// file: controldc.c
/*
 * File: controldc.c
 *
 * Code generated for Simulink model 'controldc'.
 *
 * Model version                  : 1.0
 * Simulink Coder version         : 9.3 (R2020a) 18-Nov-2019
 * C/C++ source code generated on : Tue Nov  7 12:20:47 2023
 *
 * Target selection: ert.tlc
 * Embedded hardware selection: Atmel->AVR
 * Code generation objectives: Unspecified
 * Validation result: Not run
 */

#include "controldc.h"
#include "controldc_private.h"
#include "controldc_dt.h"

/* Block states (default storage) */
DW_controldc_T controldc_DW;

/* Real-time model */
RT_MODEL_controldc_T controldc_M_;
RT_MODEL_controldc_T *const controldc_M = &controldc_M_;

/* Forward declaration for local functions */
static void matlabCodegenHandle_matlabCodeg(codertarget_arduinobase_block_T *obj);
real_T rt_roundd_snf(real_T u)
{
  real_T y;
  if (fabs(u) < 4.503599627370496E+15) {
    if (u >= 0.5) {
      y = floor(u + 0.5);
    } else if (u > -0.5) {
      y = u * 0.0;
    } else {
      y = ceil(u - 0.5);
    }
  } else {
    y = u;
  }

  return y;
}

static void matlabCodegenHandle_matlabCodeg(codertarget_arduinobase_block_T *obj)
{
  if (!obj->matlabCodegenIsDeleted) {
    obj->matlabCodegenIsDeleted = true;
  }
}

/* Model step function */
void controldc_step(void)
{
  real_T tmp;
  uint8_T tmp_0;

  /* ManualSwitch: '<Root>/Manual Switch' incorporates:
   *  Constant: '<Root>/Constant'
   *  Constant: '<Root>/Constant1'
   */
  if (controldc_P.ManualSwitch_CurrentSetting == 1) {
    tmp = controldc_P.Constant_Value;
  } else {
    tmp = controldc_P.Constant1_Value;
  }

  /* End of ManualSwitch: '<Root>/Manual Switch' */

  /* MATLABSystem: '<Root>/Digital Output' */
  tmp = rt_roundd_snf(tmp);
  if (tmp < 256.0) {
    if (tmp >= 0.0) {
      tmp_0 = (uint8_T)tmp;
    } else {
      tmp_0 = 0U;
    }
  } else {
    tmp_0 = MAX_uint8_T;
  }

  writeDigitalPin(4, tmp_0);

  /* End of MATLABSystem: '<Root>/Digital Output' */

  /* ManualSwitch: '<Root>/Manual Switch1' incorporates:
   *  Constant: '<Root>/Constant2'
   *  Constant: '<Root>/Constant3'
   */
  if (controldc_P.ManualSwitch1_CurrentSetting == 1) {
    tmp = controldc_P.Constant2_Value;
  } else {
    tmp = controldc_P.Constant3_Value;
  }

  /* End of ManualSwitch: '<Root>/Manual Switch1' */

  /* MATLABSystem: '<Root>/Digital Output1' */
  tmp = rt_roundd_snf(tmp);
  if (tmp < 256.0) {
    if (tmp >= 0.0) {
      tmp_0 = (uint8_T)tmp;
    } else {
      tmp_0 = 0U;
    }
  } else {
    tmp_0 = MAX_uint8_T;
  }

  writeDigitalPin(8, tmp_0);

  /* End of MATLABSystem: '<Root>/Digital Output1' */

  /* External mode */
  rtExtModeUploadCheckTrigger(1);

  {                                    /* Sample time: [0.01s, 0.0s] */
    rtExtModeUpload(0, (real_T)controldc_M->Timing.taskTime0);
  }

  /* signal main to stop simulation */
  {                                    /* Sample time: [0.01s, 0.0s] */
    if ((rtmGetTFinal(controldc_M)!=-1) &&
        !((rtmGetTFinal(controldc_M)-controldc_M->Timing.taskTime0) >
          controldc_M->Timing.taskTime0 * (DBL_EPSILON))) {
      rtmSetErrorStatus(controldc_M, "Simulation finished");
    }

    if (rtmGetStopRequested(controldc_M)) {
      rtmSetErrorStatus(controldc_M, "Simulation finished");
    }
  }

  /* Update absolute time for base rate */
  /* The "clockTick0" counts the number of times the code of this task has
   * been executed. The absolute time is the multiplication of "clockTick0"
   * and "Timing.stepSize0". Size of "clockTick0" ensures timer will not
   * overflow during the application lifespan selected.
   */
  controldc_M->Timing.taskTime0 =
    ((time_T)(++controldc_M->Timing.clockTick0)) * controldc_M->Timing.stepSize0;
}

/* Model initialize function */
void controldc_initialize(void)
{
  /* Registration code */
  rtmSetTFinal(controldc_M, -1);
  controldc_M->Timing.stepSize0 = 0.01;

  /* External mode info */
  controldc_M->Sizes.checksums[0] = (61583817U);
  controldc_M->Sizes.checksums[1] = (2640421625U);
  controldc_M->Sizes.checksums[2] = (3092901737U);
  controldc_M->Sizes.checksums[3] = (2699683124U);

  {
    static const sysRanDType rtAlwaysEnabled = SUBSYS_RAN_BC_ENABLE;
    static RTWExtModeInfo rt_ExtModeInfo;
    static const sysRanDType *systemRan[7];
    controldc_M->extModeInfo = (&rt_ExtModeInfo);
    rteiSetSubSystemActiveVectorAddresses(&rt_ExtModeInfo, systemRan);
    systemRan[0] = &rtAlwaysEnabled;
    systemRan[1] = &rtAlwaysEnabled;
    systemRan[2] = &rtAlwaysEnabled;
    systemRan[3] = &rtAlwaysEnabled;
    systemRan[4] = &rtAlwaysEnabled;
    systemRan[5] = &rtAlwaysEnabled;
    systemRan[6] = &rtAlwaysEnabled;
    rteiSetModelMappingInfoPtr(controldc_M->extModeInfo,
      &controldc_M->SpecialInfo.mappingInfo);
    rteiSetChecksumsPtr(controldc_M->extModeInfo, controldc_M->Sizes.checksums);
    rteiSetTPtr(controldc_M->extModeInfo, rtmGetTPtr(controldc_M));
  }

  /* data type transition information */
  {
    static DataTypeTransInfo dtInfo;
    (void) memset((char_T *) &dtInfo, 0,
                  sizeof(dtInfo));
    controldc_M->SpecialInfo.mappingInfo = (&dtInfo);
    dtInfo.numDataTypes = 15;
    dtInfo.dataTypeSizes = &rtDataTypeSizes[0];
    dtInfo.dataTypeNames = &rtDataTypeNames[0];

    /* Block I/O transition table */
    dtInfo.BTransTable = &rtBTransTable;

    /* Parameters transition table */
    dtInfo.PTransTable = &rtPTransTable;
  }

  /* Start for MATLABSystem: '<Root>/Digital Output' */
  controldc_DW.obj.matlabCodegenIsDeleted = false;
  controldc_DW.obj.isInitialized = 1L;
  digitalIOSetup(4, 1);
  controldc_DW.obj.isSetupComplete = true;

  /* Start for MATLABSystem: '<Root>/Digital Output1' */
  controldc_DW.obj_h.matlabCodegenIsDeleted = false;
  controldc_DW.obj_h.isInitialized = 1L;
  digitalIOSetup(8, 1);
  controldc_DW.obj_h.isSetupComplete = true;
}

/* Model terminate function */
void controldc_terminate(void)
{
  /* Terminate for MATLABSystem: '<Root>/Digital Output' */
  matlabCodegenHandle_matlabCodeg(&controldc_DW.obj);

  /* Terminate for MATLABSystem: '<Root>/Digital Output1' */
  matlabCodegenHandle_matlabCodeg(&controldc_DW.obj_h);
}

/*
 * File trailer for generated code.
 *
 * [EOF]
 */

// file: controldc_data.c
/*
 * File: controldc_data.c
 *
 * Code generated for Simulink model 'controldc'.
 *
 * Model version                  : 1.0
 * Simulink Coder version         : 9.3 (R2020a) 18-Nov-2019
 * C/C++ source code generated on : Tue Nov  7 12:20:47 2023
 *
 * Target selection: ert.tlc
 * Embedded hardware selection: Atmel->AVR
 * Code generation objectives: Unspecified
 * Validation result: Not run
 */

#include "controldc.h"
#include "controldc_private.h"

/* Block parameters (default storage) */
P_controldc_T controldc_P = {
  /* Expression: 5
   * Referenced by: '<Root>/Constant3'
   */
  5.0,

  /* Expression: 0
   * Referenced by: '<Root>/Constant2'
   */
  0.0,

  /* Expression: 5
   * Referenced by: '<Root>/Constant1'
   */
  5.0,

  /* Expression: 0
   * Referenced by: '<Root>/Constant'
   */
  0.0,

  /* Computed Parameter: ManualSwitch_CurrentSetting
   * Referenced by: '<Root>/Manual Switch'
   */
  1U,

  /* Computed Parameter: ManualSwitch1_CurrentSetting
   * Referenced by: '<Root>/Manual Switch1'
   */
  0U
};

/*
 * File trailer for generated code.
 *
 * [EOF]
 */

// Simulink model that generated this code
simulink model "controldc"  (R2020a)
settings: Solver=FixedStepAuto  StartTime=0.0  StopTime=inf  FixedStep=0.01  RelTol=1e-3  EnableMultiTasking=on
libraries: arduinolib x2

== system controldc ==
  Constant : Constant  Value=0
  Constant1 : Constant  Value=5
  Constant2 : Constant  Value=0
  Constant3 : Constant  Value=5
  Digital Output : arduinolib/Digital Output  pinNumber=4  Direction=output  blockPlatform=arduino
  Digital Output1 : arduinolib/Digital Output  pinNumber=8  Direction=output  blockPlatform=arduino
  Manual Switch : ManualSwitch
  Manual Switch1 : ManualSwitch
  wires:
  Constant/1 -> Manual Switch/1
  Constant1/1 -> Manual Switch/2
  Manual Switch/1 -> Digital Output/1
  Constant2/1 -> Manual Switch1/1
  Constant3/1 -> Manual Switch1/2
  Manual Switch1/1 -> Digital Output1/1
